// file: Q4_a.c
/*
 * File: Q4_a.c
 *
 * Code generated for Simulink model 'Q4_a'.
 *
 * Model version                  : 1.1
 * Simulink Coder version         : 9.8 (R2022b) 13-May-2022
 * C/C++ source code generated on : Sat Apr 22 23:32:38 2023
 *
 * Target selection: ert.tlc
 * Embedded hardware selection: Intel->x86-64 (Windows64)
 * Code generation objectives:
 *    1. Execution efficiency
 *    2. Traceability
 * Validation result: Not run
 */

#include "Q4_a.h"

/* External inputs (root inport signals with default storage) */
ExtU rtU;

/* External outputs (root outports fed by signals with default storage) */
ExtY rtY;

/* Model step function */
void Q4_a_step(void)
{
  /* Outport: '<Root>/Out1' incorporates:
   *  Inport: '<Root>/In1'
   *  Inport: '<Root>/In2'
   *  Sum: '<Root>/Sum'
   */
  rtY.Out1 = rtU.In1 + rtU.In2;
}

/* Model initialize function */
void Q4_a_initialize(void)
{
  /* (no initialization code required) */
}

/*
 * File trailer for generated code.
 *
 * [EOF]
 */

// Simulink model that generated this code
simulink model "Q4_a"  (R2022b)
settings: Solver=FixedStepDiscrete  StartTime=0.0  StopTime=10.0  RelTol=1e-3
model workspace (MATLAB code in the model file):
  | cmdLim = Simulink.Parameter;
  | cmdLim.Value = 15;
  | cmdLim.Description = 'Limit for controlling the maximum surface command angle.';
  | cmdLim.Min = 0;
  | cmdLim.Max = 90;
  | cmdLim.DocUnits = 'deg';
  | 
  | dispGain = Simulink.Parameter;
  | dispGain.Value = 0.75;
  | dispGain.Description = 'Gain applied to the displacement error.';
  | dispGain.Min = 0;
  | dispGain.Max = [];
  | dispGain.DocUnits = 'deg/sec/deg';
  | 
  | dispLim = Simulink.Parameter;
  | dispLim.Value = 30;
  | dispLim.Description = 'Limit for controlling the maximum commanded angle.';
  | dispLim.Min = 0;
  | dispLim.Max = 180;
  | dispLim.DocUnits = 'deg';
  | 
  | intGain = Simulink.Parameter;
  | intGain.Value = 0.5;
  | intGain.Description = 'Gain applied to the integral error.';
  | intGain.Min = 0;
  | intGain.Max = [];
  | intGain.DocUnits = 'deg/sec/deg/sec';
  | 
  | intLim = Simulink.Parameter;
  | intLim.Value = 5;
  | intLim.Description = 'Limit for controlling the maximum commanded angle.';
  | intLim.Min = 0;
  | intLim.Max = 90;
  | intLim.DocUnits = 'deg';
  | 
  | rateGain = Simulink.Parameter;
  | rateGain.Value = 2;
  | rateGain.Description = 'Gain applied to the rate error.';
  | rateGain.Min = 0;
  | rateGain.Max = [];
  | rateGain.DocUnits = 'deg/deg/sec';
  | 
  | rateLim = Simulink.Parameter;
  | rateLim.Value = 6;
  | rateLim.Description = 'Limit for controlling the maximum commanded angle.';
  | rateLim.Min = 0;
  | rateLim.Max = 180;
  | rateLim.DocUnits = 'deg/sec';
  | 
  | hdgGain = Simulink.Parameter;
  | hdgGain.Value = 0.015;

== system Q4_a ==
  In1 : Inport  OutDataTypeStr=single
  In2 : Inport  Port=2  OutDataTypeStr=single
  Sum : Sum  Inputs=|++  InputSameDT=on  OutDataTypeStr=Inherit: Same as first input
  Out1 : Outport  VectorParamsAs1DForOutWhenUnconnected=off
  wires:
  In1/1 -> Sum/1
  In2/1 -> Sum/2
  Sum/1 -> Out1/1
